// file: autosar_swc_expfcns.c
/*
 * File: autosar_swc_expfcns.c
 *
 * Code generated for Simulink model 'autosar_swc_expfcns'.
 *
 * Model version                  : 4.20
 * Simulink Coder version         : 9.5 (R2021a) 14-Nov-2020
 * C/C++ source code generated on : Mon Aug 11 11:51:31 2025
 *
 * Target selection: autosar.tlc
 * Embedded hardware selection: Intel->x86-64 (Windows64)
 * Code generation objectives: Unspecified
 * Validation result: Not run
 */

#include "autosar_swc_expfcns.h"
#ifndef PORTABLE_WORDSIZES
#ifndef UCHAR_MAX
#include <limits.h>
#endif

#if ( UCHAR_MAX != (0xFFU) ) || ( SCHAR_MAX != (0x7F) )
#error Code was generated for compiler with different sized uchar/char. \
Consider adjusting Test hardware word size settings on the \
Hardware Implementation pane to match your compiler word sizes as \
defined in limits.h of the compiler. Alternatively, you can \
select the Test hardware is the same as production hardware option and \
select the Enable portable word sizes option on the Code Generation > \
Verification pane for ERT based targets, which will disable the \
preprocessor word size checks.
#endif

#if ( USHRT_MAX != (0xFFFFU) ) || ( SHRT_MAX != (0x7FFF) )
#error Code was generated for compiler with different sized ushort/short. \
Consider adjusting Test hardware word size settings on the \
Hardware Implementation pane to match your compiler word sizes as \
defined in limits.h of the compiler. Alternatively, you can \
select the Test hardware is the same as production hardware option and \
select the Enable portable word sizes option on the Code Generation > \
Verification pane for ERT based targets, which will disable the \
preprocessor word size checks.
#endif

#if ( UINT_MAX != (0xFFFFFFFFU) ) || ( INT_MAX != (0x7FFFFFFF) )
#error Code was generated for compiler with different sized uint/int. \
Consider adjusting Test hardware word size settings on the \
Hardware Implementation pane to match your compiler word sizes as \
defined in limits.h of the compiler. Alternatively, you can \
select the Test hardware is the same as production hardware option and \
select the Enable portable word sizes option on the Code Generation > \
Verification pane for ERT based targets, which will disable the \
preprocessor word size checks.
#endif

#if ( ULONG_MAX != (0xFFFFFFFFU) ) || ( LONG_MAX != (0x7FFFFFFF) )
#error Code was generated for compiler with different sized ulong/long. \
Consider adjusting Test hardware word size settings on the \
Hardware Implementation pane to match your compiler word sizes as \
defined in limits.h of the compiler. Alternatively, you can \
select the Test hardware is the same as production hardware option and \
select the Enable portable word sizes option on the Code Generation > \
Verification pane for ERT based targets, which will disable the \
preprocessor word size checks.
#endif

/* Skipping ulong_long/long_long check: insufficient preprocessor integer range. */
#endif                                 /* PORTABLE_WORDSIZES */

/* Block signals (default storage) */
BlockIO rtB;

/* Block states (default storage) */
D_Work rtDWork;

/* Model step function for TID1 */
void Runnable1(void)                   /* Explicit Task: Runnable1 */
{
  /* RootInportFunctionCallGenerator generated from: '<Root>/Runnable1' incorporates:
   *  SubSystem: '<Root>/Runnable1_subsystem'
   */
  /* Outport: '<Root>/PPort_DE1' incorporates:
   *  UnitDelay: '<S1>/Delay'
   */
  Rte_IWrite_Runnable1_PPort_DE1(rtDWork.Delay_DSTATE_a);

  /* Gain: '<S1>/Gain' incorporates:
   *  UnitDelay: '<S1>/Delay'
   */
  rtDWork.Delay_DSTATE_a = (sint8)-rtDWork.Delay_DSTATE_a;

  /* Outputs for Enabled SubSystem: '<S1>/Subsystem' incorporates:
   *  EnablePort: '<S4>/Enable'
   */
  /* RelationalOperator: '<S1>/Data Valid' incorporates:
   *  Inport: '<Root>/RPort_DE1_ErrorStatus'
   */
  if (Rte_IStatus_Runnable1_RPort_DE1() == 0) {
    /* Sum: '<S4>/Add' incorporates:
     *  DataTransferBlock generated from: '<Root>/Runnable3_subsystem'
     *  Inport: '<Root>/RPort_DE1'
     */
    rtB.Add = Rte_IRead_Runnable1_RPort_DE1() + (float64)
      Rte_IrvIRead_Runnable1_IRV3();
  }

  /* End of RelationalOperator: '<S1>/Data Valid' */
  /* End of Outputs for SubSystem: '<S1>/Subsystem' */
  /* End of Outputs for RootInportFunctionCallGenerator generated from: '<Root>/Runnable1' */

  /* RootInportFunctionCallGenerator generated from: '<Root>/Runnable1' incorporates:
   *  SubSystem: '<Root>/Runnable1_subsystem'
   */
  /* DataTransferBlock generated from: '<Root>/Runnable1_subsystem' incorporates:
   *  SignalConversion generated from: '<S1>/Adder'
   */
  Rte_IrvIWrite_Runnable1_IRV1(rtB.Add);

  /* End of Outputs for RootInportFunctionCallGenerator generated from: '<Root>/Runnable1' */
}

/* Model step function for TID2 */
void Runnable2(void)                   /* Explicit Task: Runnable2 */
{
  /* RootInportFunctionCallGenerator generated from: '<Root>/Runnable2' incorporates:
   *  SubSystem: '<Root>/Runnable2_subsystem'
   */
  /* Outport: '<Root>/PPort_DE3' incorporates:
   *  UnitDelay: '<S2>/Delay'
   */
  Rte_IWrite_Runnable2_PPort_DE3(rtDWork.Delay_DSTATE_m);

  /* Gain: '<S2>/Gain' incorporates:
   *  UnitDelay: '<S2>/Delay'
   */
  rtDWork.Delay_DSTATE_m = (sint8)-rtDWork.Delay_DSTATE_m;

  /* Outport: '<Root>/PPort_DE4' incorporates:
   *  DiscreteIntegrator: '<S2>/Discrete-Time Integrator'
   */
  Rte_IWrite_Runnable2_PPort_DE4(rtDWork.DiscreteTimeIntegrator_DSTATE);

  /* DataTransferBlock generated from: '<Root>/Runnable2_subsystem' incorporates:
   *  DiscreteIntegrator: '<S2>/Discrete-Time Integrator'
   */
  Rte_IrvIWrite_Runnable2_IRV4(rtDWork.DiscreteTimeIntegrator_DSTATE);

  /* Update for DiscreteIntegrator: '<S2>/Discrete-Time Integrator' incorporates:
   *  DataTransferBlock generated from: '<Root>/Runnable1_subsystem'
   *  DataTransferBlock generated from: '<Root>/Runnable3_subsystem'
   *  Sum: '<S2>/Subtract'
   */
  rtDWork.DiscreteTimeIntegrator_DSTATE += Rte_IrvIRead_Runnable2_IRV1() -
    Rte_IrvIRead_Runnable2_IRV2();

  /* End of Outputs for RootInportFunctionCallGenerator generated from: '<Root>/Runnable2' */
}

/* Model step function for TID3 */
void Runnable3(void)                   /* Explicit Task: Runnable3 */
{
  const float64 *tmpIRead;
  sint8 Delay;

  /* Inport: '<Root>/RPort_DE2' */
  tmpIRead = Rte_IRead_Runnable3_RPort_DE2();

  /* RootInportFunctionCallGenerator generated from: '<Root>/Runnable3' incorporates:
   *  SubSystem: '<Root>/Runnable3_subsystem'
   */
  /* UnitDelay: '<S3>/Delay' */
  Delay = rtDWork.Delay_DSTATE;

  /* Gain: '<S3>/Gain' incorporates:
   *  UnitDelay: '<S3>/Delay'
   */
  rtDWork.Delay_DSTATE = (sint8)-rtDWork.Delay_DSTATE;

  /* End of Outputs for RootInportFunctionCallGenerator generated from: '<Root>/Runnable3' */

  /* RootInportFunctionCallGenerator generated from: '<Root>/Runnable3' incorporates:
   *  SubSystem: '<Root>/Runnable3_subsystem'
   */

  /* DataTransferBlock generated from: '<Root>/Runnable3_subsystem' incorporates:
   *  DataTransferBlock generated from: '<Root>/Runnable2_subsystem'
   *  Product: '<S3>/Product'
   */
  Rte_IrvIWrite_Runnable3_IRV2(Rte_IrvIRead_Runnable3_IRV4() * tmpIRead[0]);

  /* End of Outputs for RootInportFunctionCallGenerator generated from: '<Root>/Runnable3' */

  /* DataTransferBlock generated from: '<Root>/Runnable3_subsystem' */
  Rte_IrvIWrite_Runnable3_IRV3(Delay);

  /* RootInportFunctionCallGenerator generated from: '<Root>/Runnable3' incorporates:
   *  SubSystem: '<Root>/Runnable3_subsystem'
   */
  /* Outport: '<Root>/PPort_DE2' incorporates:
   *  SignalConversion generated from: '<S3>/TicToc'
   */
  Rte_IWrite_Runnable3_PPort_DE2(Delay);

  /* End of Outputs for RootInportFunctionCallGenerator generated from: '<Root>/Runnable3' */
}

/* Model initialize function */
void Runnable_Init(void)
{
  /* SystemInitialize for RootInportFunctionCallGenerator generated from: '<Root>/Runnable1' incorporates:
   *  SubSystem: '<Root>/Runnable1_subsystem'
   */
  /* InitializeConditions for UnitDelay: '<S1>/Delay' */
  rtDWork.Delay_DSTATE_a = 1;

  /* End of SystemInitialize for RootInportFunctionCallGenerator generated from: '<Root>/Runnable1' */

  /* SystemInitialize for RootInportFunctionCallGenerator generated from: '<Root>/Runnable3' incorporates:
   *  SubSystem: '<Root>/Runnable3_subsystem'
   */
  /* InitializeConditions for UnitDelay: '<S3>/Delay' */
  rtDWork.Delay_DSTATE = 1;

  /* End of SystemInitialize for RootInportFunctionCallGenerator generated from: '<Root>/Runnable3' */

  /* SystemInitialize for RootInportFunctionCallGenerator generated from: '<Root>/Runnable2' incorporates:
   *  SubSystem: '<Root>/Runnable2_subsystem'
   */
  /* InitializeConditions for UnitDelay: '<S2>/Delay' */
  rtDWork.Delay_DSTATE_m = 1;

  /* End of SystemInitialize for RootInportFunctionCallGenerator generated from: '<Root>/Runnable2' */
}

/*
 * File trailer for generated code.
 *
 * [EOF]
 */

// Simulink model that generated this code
simulink model "autosar_swc_expfcns"  (R2021a)
settings: Solver=FixedStepDiscrete  StartTime=0.0  StopTime=20  FixedStep=1  MaxStep=.0001  RelTol=1e-3  EnableMultiTasking=on
undefined symbols (not defined in the file): DiscIntNeverNeededParam

== system autosar_swc_expfcns ==
  note: This component model implements AUTOSAR runnable entities using exported functions.
  note: Copyright 2008-2018 The MathWorks, Inc.
  Runnable1 : Inport  PortDimensions=1  SampleTime=1  OutputFunctionCall=on
  Runnable2 : Inport  Port=2  PortDimensions=1  SampleTime=1  OutputFunctionCall=on
  Runnable3 : Inport  Port=3  PortDimensions=1  SampleTime=10  OutputFunctionCall=on
  RPort_DE1 : Inport  Port=4  OutDataTypeStr=double  PortDimensions=1
  RPort_DE1_ErrorStatus : Inport  Port=5  OutDataTypeStr=uint8  PortDimensions=1
  RPort_DE2 : Inport  Port=6  OutDataTypeStr=double  PortDimensions=2
  Runnable1_subsystem : Subsystem  TreatAsAtomicUnit=on  RTWFcnName=foo
  Runnable2_subsystem : Subsystem  TreatAsAtomicUnit=on  RTWFcnName=foo
  Runnable3_subsystem : Subsystem  TreatAsAtomicUnit=on  RTWFcnName=foo
  Scope1 : Scope
  Scope2 : Scope
  Scope3 : Scope  NumInputPorts=2
  PPort_DE1 : Outport  OutDataTypeStr=int8  PortDimensions=1  VectorParamsAs1DForOutWhenUnconnected=off
  PPort_DE2 : Outport  Port=2  OutDataTypeStr=int8  PortDimensions=1  VectorParamsAs1DForOutWhenUnconnected=off
  PPort_DE3 : Outport  Port=3  OutDataTypeStr=int8  PortDimensions=2  VectorParamsAs1DForOutWhenUnconnected=off
  PPort_DE4 : Outport  Port=4  OutDataTypeStr=double  PortDimensions=1  VectorParamsAs1DForOutWhenUnconnected=off
  wires:
  [B] -> Runnable1_subsystem/3(In2)  "irv3"
  Runnable3_subsystem/1(TicToc_irv) -> [B]
  [A] -> Runnable2_subsystem/2(In2)
  Runnable3_subsystem/3(Multiplier) -> [A]  "irv2"
  RPort_DE1_ErrorStatus/1 -> Runnable1_subsystem/2(ErrorStatus)
  Runnable2_subsystem/2(Subtracter) -> Scope3/1, PPort_DE4/1
  RPort_DE1/1 -> Runnable1_subsystem/1(In1)
  Runnable2/1 -> Runnable2_subsystem/Trigger
  Runnable1_subsystem/1(TicToc) -> Scope1/1, PPort_DE1/1
  Runnable2_subsystem/1(TicToc) -> Scope2/1, PPort_DE3/1
  Runnable3_subsystem/2(TicToc) -> Scope3/2, PPort_DE2/1
  Runnable1/1 -> Runnable1_subsystem/Trigger
  Runnable1_subsystem/2(Adder) -> Runnable2_subsystem/1(In1)  "irv1"
  Runnable2_subsystem/3(Subtracter_irv) -> Runnable3_subsystem/1(In1)  "irv4"
  RPort_DE2/1 -> Runnable3_subsystem/2(In2)
  Runnable3/1 -> Runnable3_subsystem/Trigger

== system autosar_swc_expfcns/Runnable1_subsystem ==
  In1 : Inport
  ErrorStatus : Inport  Port=2
  In2 : Inport  Port=3
  function : TriggerPort  TriggerType=function-call  VariantControl=Variant  SampleTimeType=periodic  SampleTime=-1
  Data Valid : RelationalOperator  Operator===  OutDataTypeStr=boolean  RndMeth=Nearest
  Delay : UnitDelay  InitialCondition=1  SampleTime=-1  HasFrameUpgradeWarning=on
  Gain : Gain  Gain=-1  OutDataTypeStr=fixdt(1,8,0)
  RTE_E_OK : Constant  Value=0
  Subsystem : Subsystem
  TicToc : Outport  InitialOutput=0  VectorParamsAs1DForOutWhenUnconnected=off
  Adder : Outport  Port=2  InitialOutput=0  VectorParamsAs1DForOutWhenUnconnected=off
  wires:
  RTE_E_OK/1 -> Data Valid/2
  ErrorStatus/1 -> Data Valid/1
  Data Valid/1 -> Subsystem/Enable
  In2/1 -> Subsystem/2(In2)
  In1/1 -> Subsystem/1(In1)
  Delay/1 -> Gain/1, TicToc/1
  Gain/1 -> Delay/1
  Subsystem/1(Adder) -> Adder/1

== system autosar_swc_expfcns/Runnable2_subsystem ==
  In1 : Inport
  In2 : Inport  Port=2
  function : TriggerPort  TriggerType=function-call  VariantControl=Variant  SampleTimeType=periodic  SampleTime=-1
  Delay : UnitDelay  InitialCondition=1  SampleTime=-1  HasFrameUpgradeWarning=on
  Discrete-Time Integrator : DiscreteIntegrator  SampleTime=-1  ICPrevOutput=DiscIntNeverNeededParam  ICPrevScaledInput=DiscIntNeverNeededParam
  Gain : Gain  Gain=-1  OutDataTypeStr=fixdt(1,8,0)
  Subtract : Sum  Inputs=+-
  TicToc : Outport  InitialOutput=0  VectorParamsAs1DForOutWhenUnconnected=off
  Subtracter : Outport  Port=2  InitialOutput=0  VectorParamsAs1DForOutWhenUnconnected=off
  Subtracter_irv : Outport  Port=3  VectorParamsAs1DForOutWhenUnconnected=off
  wires:
  Discrete-Time Integrator/1 -> Subtracter/1, Subtracter_irv/1
  Subtract/1 -> Discrete-Time Integrator/1
  Gain/1 -> Delay/1
  Delay/1 -> TicToc/1, Gain/1
  In1/1 -> Subtract/1
  In2/1 -> Subtract/2

== system autosar_swc_expfcns/Runnable3_subsystem ==
  In1 : Inport  OutDataTypeStr=double
  In2 : Inport  Port=2
  function : TriggerPort  TriggerType=function-call  VariantControl=Variant  SampleTimeType=periodic  SampleTime=-1
  Delay : UnitDelay  InitialCondition=1  SampleTime=-1  HasFrameUpgradeWarning=on
  Gain : Gain  Gain=-1  OutDataTypeStr=fixdt(1,8,0)
  Product : Product  Inputs=**  OutDataTypeStr=Inherit: Same as first input
  Selector : Selector  InputPortWidth=2  IndexOptions=Index vector (dialog)  Indices=1  OutputSizes=1
  TicToc_irv : Outport  VectorParamsAs1DForOutWhenUnconnected=off
  TicToc : Outport  Port=2  InitialOutput=0  VectorParamsAs1DForOutWhenUnconnected=off
  Multiplier : Outport  Port=3  InitialOutput=0  VectorParamsAs1DForOutWhenUnconnected=off
  wires:
  Selector/1 -> Product/2
  Product/1 -> Multiplier/1
  Gain/1 -> Delay/1
  Delay/1 -> TicToc_irv/1, TicToc/1, Gain/1
  In1/1 -> Product/1
  In2/1 -> Selector/1

== system autosar_swc_expfcns/Runnable1_subsystem/Subsystem ==
  In1 : Inport
  In2 : Inport  Port=2
  Enable : EnablePort
  Add : Sum
  Adder : Outport  VectorParamsAs1DForOutWhenUnconnected=off
  wires:
  In2/1 -> Add/2
  In1/1 -> Add/1
  Add/1 -> Adder/1
